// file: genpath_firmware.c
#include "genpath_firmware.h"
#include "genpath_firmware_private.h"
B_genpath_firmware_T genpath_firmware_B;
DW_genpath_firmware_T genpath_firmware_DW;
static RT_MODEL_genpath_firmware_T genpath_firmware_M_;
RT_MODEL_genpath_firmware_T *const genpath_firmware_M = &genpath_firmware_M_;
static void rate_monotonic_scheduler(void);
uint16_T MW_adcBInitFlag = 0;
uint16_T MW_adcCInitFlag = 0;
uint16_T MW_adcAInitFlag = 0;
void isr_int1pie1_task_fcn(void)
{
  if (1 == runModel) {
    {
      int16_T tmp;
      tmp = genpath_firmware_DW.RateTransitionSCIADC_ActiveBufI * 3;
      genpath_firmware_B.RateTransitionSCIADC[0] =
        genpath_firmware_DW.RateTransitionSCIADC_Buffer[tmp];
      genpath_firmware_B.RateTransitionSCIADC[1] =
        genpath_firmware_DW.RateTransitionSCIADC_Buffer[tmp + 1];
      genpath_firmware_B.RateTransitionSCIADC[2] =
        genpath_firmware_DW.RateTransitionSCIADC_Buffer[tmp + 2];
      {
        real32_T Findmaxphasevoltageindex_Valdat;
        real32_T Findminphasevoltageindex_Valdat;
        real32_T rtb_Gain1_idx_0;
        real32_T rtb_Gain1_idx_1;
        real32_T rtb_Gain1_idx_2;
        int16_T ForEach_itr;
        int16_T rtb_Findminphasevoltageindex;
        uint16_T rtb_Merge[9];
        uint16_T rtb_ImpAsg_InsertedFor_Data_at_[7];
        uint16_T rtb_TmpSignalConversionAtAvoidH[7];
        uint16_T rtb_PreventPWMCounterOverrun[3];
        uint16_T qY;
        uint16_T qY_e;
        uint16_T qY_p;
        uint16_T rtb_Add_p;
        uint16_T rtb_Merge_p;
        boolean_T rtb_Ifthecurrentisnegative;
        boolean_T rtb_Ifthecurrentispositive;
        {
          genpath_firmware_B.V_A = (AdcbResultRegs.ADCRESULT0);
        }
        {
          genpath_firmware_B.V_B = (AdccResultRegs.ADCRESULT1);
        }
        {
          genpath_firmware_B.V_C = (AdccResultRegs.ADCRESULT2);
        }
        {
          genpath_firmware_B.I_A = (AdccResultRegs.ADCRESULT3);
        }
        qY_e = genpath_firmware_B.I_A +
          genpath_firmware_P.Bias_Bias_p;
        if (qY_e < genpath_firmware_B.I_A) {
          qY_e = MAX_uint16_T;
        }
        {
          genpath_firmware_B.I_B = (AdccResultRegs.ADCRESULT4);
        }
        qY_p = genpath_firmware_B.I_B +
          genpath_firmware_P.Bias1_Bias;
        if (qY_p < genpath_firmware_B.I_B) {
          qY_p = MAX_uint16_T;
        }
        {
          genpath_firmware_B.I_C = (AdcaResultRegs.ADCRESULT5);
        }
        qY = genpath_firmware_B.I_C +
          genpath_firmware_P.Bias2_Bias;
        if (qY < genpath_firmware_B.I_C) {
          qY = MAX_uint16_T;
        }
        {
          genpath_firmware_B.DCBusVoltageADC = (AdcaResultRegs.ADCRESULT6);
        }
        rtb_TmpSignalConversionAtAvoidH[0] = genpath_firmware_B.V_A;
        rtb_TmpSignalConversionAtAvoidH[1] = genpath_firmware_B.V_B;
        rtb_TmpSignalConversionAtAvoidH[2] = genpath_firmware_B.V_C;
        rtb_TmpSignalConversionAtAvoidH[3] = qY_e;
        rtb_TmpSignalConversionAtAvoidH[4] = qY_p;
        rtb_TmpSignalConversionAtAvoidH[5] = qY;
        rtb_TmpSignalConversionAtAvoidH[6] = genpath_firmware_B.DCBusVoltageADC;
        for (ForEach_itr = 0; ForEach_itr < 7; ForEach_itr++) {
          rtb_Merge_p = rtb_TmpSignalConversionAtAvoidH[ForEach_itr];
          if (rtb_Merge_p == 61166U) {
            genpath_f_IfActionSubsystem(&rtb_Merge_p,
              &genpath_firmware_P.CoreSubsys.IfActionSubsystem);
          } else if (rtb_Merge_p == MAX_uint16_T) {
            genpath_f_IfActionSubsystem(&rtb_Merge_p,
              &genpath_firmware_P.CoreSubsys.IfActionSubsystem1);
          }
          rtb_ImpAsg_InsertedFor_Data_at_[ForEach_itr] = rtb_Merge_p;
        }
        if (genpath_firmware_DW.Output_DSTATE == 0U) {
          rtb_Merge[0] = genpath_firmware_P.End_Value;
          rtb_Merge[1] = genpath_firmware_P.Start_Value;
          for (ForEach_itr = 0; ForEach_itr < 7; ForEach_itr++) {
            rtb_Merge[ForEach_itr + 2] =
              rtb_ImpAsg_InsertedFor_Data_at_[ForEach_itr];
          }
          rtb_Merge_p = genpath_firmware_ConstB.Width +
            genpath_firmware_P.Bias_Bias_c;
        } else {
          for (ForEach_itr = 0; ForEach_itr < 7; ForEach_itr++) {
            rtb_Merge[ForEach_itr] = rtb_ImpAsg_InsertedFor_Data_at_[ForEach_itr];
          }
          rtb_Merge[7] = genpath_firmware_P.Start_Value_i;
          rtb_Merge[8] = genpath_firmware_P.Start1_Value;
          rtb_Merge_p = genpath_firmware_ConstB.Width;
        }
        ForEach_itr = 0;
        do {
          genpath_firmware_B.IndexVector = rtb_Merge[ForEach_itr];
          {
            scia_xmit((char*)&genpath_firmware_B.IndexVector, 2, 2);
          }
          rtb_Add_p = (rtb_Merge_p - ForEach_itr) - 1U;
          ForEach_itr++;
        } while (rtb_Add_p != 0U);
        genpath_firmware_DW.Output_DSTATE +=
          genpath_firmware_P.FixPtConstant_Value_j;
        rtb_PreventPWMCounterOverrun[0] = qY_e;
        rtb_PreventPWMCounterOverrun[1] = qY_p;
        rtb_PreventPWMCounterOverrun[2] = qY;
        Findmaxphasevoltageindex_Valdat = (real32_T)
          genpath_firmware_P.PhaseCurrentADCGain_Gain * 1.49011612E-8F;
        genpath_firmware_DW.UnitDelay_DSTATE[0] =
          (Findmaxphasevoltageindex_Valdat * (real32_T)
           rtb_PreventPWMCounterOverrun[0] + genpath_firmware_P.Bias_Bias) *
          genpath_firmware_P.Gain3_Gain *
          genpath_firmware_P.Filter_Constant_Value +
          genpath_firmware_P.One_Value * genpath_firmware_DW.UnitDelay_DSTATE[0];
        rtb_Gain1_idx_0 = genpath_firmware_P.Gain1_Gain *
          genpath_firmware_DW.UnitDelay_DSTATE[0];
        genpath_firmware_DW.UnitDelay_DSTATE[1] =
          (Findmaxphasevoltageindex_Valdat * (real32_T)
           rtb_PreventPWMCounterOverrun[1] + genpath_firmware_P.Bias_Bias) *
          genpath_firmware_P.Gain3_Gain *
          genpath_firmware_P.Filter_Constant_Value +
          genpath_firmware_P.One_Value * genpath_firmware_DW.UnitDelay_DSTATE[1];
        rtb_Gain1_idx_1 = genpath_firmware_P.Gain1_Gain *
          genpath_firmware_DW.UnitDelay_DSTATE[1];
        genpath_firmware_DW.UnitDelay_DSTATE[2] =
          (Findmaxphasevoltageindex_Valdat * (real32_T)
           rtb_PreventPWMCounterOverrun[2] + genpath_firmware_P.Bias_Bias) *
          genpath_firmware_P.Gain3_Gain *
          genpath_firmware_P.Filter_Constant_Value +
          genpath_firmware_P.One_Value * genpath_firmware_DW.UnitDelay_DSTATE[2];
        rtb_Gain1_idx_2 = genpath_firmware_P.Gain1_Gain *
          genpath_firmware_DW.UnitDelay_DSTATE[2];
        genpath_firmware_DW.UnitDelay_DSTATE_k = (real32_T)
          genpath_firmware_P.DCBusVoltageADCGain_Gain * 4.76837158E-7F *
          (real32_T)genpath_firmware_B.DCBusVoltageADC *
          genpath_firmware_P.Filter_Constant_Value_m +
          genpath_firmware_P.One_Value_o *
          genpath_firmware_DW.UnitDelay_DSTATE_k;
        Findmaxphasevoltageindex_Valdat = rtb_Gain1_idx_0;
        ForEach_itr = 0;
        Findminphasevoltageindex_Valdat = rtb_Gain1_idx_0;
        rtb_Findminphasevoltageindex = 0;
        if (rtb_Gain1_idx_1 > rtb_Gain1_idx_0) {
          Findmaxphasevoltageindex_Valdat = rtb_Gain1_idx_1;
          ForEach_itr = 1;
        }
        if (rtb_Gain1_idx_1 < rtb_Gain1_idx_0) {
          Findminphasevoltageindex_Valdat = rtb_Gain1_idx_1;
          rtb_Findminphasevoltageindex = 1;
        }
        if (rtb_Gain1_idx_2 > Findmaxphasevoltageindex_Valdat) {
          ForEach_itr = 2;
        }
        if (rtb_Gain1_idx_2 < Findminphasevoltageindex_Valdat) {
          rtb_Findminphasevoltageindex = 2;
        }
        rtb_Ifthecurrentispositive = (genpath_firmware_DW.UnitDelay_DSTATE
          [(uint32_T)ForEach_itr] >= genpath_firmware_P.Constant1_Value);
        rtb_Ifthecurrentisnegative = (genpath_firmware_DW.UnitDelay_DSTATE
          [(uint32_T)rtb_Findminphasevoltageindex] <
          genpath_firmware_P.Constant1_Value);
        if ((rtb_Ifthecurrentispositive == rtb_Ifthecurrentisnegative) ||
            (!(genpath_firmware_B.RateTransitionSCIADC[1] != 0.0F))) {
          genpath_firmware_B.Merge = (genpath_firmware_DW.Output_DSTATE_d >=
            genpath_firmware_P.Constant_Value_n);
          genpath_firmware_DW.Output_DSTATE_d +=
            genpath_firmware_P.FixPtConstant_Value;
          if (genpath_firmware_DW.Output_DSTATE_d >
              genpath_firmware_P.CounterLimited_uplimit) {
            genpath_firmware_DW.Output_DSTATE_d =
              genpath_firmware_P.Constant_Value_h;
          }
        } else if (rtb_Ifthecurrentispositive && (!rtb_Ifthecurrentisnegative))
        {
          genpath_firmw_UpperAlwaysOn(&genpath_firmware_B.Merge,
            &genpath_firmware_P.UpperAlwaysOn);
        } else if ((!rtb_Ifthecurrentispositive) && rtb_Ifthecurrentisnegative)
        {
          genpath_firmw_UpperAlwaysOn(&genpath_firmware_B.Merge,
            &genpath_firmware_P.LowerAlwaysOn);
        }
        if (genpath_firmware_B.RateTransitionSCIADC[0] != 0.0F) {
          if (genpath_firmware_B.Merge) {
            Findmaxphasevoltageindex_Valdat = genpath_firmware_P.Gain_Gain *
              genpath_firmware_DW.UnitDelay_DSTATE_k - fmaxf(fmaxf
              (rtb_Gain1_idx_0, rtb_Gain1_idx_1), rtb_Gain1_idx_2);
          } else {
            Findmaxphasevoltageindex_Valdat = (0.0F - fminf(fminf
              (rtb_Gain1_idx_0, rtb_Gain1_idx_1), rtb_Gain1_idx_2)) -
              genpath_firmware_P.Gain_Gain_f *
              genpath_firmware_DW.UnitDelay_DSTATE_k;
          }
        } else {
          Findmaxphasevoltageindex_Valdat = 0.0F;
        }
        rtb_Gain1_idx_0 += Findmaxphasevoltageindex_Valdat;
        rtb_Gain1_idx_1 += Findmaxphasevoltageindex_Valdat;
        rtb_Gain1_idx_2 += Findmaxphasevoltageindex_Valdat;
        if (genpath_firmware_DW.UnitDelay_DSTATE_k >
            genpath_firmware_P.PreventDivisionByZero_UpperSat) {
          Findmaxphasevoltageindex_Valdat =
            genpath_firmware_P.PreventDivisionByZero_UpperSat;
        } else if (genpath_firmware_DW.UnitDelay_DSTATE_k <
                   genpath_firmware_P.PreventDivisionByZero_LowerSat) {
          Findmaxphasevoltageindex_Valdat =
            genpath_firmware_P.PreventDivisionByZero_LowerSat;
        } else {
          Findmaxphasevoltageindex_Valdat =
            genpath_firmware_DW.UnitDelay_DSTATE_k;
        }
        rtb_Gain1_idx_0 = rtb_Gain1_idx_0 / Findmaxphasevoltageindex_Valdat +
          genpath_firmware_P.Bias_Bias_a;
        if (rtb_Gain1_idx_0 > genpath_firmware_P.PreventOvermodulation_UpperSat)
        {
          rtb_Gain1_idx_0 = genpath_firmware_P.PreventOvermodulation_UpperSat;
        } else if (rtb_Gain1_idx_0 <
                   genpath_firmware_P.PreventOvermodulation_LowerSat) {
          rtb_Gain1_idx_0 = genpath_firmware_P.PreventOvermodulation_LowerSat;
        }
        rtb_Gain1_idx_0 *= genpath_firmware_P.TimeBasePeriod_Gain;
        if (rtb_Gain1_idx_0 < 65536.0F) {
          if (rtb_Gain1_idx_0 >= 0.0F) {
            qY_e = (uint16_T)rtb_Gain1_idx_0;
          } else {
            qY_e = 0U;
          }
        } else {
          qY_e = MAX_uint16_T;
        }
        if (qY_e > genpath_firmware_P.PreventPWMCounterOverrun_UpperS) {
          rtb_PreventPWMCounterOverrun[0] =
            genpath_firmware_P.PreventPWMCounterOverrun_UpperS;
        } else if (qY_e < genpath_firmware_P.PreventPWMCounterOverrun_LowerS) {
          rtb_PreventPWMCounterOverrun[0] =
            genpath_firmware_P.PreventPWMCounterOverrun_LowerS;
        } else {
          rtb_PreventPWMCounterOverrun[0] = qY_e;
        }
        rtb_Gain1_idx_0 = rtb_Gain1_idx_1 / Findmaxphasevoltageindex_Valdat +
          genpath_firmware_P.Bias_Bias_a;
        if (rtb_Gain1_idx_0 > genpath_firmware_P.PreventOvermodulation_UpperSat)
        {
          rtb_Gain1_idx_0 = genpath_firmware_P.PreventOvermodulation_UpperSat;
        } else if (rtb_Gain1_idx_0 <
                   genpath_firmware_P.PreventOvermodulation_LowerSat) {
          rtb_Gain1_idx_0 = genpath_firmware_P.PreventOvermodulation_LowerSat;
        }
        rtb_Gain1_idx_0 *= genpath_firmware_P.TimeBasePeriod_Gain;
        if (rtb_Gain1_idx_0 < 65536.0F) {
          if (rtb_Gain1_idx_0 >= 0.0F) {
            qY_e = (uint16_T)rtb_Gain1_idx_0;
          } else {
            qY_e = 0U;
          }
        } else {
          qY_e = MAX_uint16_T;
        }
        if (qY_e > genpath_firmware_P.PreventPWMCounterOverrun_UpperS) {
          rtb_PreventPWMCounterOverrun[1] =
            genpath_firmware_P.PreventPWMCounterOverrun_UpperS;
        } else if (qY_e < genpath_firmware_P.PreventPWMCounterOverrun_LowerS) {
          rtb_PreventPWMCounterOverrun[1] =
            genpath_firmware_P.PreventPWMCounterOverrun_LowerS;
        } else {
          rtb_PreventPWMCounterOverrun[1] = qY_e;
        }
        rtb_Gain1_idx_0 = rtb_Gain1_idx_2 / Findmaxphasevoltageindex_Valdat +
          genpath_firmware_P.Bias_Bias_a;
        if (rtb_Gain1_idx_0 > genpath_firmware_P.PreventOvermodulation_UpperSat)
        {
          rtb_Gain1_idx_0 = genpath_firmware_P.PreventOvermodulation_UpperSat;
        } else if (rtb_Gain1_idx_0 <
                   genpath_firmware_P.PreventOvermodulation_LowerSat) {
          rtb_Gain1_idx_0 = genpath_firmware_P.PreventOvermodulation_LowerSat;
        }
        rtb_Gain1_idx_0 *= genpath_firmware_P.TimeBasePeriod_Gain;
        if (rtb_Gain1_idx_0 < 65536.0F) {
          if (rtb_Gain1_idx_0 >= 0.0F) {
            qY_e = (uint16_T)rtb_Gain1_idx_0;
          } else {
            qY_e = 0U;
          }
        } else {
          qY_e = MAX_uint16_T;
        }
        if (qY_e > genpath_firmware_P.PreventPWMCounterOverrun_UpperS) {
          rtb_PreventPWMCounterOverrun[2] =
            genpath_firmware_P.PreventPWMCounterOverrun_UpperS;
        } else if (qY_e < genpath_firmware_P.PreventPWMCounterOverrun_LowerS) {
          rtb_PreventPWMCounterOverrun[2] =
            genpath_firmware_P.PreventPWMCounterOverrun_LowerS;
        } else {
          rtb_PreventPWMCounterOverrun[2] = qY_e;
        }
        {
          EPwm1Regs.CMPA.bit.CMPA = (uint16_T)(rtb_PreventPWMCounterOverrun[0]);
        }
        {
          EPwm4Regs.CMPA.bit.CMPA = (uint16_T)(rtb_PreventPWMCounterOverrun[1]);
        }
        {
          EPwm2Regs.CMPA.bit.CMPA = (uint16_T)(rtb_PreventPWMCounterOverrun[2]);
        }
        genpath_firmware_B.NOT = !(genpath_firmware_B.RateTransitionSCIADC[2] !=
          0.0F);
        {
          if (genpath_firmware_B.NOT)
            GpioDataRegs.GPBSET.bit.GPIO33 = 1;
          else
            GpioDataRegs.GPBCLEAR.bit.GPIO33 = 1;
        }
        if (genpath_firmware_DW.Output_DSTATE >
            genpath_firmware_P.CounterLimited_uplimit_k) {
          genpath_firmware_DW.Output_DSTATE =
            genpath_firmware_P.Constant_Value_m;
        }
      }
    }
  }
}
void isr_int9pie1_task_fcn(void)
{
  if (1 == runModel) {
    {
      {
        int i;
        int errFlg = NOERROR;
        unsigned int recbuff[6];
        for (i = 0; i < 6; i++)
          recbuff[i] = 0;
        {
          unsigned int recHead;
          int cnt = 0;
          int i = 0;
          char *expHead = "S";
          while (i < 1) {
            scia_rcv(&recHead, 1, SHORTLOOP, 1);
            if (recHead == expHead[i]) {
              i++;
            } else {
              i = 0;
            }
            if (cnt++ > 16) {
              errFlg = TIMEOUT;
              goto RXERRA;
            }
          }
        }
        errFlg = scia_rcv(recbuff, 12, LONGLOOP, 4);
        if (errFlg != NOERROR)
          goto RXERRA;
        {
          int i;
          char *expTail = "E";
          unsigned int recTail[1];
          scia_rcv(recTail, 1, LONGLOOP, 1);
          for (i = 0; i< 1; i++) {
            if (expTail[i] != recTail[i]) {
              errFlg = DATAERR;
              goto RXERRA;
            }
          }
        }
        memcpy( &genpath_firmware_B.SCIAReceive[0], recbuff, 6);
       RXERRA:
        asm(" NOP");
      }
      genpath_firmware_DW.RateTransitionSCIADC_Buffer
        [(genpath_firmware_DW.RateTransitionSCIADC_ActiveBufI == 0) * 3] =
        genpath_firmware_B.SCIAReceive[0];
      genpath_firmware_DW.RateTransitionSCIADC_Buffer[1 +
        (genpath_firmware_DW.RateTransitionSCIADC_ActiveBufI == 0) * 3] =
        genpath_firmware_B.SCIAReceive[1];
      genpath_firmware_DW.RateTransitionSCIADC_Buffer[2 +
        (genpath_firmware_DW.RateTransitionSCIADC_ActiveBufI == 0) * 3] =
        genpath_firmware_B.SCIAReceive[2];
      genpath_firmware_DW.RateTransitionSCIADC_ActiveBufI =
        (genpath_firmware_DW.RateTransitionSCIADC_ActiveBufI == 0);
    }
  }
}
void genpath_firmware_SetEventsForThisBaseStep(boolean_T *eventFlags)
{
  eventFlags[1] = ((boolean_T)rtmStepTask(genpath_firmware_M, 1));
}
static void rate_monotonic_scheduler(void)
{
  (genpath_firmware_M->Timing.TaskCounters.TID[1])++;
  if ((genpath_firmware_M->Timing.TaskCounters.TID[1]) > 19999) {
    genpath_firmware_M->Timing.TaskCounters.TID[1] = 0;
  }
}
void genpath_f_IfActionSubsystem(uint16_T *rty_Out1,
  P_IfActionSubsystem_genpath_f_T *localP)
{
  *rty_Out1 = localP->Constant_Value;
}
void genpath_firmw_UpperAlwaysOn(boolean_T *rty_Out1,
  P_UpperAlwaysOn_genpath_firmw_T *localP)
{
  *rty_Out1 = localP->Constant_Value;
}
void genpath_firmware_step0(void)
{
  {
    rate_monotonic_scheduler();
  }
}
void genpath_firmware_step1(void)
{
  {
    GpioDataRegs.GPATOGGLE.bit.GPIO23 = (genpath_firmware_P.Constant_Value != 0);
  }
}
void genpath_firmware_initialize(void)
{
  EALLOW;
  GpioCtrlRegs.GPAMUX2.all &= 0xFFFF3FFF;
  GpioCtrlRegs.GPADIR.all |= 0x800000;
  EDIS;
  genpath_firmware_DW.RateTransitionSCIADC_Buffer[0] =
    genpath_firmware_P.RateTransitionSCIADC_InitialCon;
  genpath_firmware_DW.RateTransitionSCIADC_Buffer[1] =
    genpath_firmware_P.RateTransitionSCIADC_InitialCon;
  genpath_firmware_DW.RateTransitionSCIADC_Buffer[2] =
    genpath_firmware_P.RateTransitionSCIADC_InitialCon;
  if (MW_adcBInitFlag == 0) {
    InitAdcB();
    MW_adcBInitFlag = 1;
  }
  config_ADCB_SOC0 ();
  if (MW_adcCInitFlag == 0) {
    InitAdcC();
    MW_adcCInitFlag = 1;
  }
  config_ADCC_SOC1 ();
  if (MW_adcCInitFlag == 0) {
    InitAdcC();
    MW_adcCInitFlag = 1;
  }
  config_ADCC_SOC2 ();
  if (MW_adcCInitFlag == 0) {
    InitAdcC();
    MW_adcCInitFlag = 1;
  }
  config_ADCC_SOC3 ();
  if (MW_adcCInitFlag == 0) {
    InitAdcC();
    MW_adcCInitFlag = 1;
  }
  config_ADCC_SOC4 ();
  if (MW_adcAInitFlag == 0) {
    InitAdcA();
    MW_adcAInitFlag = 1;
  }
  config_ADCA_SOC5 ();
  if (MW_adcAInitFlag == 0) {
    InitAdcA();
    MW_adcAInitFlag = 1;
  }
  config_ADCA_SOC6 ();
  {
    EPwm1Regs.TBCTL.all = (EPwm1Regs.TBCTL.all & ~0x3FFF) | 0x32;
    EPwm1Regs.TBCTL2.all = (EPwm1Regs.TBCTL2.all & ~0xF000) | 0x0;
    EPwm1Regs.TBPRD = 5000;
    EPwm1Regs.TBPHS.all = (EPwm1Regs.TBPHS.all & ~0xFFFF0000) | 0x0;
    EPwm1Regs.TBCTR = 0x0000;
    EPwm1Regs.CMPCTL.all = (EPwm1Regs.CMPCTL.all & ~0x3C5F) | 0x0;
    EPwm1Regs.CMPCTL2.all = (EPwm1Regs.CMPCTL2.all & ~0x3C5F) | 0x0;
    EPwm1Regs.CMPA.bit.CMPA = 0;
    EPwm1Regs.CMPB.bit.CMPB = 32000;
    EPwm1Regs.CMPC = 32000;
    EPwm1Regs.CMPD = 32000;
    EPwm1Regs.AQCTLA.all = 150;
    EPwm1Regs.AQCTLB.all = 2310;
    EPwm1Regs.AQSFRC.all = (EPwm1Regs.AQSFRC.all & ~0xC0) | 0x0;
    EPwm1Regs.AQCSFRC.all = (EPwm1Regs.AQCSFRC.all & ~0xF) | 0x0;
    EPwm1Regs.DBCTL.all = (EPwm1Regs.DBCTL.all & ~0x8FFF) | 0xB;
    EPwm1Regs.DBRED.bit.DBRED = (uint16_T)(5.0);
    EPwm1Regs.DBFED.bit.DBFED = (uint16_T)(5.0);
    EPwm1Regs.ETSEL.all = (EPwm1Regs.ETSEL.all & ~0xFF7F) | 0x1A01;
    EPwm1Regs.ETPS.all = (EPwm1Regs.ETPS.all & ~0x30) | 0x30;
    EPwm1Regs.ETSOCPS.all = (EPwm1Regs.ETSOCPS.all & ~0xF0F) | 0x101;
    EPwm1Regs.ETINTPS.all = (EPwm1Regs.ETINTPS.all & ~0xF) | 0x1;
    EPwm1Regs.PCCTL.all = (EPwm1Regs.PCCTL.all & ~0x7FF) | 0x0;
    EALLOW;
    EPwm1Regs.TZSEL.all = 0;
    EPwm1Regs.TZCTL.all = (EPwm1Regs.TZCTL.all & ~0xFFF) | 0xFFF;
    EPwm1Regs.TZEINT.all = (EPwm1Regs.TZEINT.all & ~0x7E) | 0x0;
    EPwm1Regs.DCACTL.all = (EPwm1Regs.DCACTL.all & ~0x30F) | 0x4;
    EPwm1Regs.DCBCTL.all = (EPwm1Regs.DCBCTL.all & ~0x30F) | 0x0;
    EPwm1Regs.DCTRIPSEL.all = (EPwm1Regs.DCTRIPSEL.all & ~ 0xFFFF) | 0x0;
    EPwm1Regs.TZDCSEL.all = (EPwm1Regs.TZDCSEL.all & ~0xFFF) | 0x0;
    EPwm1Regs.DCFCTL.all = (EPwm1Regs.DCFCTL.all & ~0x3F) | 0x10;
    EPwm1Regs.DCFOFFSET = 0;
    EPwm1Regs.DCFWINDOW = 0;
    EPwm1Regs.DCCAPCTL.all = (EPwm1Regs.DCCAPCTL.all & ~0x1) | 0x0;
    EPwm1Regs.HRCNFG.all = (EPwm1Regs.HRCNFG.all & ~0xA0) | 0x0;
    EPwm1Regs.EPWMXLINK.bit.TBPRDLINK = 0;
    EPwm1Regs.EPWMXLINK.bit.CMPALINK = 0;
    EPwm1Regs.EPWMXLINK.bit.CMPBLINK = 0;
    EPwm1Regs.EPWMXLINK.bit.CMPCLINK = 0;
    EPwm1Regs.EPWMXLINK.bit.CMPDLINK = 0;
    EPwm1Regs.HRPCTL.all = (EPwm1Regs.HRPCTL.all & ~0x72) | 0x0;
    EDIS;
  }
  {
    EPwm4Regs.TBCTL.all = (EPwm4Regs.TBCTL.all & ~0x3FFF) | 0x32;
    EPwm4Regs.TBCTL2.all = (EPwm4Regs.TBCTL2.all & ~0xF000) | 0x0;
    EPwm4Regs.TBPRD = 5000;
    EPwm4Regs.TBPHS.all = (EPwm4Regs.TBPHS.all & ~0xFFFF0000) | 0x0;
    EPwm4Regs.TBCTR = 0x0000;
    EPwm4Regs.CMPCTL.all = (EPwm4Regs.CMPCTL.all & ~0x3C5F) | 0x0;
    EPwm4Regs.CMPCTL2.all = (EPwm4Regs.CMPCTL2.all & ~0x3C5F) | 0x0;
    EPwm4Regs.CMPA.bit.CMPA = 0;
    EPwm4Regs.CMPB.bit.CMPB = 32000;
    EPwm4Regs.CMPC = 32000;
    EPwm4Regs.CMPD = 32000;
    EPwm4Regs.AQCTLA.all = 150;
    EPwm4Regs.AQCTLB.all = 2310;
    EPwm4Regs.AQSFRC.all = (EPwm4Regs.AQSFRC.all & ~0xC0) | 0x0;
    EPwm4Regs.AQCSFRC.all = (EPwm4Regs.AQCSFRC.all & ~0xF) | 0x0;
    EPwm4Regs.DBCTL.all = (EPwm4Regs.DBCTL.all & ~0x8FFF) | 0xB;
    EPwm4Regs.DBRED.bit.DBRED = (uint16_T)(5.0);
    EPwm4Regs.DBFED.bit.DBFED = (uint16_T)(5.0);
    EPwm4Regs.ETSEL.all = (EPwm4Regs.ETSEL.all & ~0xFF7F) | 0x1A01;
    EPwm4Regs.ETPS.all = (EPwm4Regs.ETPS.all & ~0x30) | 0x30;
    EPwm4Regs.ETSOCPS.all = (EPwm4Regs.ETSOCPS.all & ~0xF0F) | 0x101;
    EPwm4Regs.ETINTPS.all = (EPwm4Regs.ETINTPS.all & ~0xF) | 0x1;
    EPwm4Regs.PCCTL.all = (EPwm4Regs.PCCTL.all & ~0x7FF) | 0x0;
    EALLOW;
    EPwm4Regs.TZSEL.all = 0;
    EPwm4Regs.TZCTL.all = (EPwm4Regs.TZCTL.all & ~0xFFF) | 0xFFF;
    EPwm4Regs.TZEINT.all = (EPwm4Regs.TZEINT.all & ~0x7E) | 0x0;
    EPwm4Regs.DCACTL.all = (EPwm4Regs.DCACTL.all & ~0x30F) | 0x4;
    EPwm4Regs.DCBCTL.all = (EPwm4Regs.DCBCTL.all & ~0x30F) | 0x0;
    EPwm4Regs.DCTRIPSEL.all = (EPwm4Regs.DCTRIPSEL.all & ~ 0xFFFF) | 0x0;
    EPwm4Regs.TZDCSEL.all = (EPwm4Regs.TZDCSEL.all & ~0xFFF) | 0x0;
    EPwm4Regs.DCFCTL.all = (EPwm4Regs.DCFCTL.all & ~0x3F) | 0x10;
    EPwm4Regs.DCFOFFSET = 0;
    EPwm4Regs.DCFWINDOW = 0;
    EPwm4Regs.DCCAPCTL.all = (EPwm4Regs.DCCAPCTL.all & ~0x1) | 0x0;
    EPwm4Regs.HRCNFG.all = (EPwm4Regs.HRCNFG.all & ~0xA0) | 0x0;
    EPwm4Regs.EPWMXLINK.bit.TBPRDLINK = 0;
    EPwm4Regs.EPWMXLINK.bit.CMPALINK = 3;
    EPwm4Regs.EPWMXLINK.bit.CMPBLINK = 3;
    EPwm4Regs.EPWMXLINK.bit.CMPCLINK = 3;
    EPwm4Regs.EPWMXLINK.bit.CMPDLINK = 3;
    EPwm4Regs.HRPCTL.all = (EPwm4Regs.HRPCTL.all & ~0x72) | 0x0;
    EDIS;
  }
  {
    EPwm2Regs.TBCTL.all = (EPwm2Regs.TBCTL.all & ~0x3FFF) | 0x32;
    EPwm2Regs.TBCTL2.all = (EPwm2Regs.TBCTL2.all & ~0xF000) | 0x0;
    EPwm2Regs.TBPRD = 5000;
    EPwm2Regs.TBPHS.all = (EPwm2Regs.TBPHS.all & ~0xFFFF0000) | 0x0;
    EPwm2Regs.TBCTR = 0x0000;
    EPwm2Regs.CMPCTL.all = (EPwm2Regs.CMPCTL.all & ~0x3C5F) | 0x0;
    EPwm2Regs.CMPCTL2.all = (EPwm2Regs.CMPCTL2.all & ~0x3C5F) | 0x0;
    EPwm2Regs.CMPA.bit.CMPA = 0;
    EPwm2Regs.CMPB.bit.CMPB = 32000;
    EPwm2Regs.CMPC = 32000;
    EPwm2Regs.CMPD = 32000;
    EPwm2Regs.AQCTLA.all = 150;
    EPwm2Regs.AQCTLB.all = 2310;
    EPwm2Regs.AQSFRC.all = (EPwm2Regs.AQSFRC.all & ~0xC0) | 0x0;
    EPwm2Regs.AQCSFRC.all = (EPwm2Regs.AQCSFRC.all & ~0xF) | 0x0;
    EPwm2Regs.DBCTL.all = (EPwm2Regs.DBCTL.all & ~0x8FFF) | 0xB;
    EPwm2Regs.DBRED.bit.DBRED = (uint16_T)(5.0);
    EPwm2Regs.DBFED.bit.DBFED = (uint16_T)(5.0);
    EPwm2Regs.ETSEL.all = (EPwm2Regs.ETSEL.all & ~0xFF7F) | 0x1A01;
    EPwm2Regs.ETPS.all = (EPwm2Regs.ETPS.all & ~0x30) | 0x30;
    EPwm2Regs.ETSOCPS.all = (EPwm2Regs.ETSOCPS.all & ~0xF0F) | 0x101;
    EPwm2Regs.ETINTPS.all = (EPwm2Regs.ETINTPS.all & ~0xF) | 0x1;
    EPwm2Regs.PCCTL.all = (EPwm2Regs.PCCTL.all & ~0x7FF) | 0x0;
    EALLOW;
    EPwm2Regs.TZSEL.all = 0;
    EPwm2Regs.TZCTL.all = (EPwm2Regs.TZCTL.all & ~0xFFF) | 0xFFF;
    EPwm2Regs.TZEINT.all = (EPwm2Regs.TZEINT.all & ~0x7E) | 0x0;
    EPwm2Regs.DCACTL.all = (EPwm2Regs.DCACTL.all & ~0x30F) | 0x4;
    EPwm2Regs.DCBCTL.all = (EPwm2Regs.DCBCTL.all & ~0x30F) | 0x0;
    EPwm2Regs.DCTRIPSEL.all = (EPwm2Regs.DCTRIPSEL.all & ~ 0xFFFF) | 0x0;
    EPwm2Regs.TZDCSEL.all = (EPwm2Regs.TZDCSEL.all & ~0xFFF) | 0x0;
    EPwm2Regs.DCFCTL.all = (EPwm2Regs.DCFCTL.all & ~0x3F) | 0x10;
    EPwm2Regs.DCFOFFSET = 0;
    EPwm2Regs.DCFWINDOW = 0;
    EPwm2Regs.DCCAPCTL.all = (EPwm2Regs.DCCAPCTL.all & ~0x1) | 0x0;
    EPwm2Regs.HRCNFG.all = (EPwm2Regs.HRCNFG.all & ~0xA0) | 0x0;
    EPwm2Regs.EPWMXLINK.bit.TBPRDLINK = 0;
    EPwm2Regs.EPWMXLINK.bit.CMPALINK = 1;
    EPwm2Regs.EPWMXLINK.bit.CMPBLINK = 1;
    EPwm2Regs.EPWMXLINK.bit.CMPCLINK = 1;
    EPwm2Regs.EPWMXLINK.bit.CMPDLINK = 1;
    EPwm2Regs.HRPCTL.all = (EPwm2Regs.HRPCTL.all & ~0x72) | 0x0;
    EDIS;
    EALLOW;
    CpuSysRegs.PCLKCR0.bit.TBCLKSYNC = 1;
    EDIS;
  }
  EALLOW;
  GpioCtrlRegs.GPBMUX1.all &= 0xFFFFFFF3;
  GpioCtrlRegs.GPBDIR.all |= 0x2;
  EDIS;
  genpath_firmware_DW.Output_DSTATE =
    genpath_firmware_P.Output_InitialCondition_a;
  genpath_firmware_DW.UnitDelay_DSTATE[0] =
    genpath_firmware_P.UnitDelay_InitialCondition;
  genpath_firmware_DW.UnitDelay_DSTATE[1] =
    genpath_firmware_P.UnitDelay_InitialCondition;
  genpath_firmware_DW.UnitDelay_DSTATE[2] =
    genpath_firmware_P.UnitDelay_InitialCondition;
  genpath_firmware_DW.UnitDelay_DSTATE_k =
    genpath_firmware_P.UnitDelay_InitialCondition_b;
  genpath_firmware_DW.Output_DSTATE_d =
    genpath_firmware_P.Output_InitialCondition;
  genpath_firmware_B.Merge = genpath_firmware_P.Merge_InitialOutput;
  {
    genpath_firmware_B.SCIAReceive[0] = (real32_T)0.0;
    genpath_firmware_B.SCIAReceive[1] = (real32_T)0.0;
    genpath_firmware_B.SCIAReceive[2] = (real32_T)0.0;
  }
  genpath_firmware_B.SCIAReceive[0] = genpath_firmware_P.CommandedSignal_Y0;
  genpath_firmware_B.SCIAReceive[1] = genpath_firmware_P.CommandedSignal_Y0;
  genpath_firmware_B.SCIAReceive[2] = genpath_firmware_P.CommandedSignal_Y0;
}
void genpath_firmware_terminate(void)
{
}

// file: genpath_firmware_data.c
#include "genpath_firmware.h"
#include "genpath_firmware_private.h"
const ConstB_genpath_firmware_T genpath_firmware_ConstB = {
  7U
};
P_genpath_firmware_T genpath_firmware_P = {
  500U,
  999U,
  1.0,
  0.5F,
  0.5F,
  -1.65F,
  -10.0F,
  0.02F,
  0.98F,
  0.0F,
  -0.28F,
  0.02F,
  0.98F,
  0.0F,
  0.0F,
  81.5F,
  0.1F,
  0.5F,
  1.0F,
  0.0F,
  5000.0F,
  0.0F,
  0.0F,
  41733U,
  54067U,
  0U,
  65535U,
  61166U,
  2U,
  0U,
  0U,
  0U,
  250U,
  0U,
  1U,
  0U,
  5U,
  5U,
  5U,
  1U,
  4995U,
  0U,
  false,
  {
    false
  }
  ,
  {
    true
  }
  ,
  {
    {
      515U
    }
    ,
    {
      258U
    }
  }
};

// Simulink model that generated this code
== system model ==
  Subsystem#1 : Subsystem  <- 1: RateTransitionSCIADC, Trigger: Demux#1
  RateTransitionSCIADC : RateTransition  <- 1: Subsystem#2
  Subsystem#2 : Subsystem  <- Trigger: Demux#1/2
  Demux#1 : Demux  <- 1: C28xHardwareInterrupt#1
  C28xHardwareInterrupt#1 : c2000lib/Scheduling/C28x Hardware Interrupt
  DigitalOutput#1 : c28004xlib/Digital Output  <- 1: Constant
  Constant : Constant
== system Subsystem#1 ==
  CommandedSignal : Inport
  TriggerPort#1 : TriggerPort  TriggerType=function-call
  IIRFilter#1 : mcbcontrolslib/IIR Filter  <- 1: Gain#1
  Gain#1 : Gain  Gain=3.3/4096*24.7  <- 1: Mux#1
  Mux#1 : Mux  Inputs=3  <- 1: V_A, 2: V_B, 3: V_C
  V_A : c2802xlib/ADC
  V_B : c2802xlib/ADC
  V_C : c2802xlib/ADC
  Subsystem#3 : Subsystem  <- 1: Merge, 2: Merge#1
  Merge : Merge  <- 1: Start, 2: Data
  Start : Subsystem  <- 1: Subsystem#4, 2: Width, Action: If#1
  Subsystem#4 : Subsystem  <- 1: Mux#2
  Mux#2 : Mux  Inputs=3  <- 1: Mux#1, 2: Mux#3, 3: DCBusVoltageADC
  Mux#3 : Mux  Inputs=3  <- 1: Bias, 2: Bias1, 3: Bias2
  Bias : Bias  Bias=+5  <- 1: I_A
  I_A : c2802xlib/ADC
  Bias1 : Bias  Bias=+5  <- 1: I_B
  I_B : c2802xlib/ADC
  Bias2 : Bias  Bias=+5  <- 1: I_C
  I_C : c2802xlib/ADC
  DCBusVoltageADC : c2802xlib/ADC
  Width : Width  <- 1: Subsystem#4
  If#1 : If  IfExpression=u1 == 0  <- 1: CounterLimited
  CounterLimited : simulink/Sources/Counter Limited  uplimit=999
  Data : Subsystem  <- 1: Subsystem#4, 2: Width, Action: If#1/2
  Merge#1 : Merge  <- 1: Start/2, 2: Data/2
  ePWM#1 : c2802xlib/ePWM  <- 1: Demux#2
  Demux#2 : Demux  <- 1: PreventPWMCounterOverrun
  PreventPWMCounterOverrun : Saturate  UpperLimit=4995  LowerLimit=0  <- 1: DataTypeConversion#1
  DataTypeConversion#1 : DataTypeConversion  <- 1: TimeBasePeriod
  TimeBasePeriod : Gain  Gain=5000  <- 1: PreventOvermodulation
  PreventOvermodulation : Saturate  UpperLimit=1  LowerLimit=0  <- 1: Bias#1
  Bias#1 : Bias  Bias=0.5  <- 1: Product#1
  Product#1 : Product  Inputs=*/  <- 1: Add, 2: PreventDivisionByZero
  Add : Sum  <- 1: Gain1, 2: Merge#2
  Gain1 : Gain  Gain=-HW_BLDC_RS  <- 1: IIRFilter#2
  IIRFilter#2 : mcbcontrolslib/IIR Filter  <- 1: Gain3
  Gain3 : Gain  Gain=-10  <- 1: Bias#2
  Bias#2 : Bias  Bias=-1.65  <- 1: PhaseCurrentADCGain
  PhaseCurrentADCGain : Gain  Gain=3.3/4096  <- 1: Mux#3
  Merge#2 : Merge  <- 1: Subsystem#5, 2: Subsystem#6
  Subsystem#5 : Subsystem  <- 1: Gain1, 2: IIRFilter#3, 3: Merge#3, Action: If#2
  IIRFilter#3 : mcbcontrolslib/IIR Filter  <- 1: DCBusVoltageADCGain
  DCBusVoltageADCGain : Gain  Gain=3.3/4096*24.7  <- 1: DCBusVoltageADC
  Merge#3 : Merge  Inputs=3  <- 1: Subsystem#7, 2: UpperAlwaysOn, 3: LowerAlwaysOn
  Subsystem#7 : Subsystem  <- Action: If#3
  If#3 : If  IfExpression=(u1 == u2) | ~u3  ElseIfExpressions=u1 & ~u2,~u1 & u2  <- 1: Ifthecurrentispositive, 2: Ifthecurrentisnegative, 3: DataTypeConversion#2
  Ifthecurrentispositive : RelationalOperator  <- 1: MultiPortSwitch#1, 2: Constant1
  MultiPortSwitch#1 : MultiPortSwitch  DataPortOrder=Zero-based contiguous  Inputs=1  <- 1: Findmaxphasevoltageindex, 2: IIRFilter#2
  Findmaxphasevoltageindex : dspstat3/Maximum  <- 1: Gain1
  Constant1 : Constant  Value=0
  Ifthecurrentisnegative : RelationalOperator  Operator=<  <- 1: MultiPortSwitch#2, 2: Constant1
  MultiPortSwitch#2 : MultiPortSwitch  DataPortOrder=Zero-based contiguous  Inputs=1  <- 1: Findminphasevoltageindex, 2: IIRFilter#2
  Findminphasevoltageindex : dspstat3/Minimum  <- 1: Gain1
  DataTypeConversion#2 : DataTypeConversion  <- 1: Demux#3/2
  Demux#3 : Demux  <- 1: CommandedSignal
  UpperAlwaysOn : Subsystem  <- Action: If#3/2
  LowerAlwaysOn : Subsystem  <- Action: If#3/3
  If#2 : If  IfExpression=u1  <- 1: DataTypeConversion#3
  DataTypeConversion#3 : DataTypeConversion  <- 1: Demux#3
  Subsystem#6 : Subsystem  <- Action: If#2/2
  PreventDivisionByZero : Saturate  UpperLimit=81.5  LowerLimit=0.1  <- 1: IIRFilter#3
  ePWM#2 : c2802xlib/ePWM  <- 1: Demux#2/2
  ePWM#3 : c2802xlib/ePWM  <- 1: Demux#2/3
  DigitalOutput#2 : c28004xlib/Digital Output  <- 1: NOT
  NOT : Logic  Operator=NOT  <- 1: DataTypeConversion#4
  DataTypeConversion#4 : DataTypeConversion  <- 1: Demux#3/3
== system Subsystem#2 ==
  TriggerPort#2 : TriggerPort  TriggerType=function-call
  Outport#1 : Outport  <- 1: SCIAReceive
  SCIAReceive : c280xlib/SCI Receive
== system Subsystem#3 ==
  Inport#1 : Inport
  Inport#2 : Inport
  WhileIterator#1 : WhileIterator  MaxIters=-1  WhileBlockType=do-while  <- 1: Sum#1
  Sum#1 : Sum  Inputs=+-  <- 1: Inport#2, 2: WhileIterator#1
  SCITransmit#1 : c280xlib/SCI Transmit  <- 1: IndexVector
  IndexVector : MultiPortSwitch  Inputs=1  <- 1: WhileIterator#1, 2: Inport#1
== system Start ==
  Inport#3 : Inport
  Inport#4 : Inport
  ActionPort#1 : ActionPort
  Outport#2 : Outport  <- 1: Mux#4
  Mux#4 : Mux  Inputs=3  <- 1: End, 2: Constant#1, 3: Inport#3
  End : Constant  Value=65535
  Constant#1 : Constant  Value=61166
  Outport#3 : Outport  <- 1: Bias#3
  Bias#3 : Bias  Bias=2  <- 1: Inport#4
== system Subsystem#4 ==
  Inport#5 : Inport
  ForEach : ForEach
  Outport#4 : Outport  <- 1: Merge#4
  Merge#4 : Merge  Inputs=3  <- 1: IfActionSubsystem, 2: IfActionSubsystem1, 3: Subsystem#8
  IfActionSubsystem : Subsystem  <- Action: If#4
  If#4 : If  IfExpression=u1 == 61166  ElseIfExpressions=u1 == 65535  <- 1: Inport#5
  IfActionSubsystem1 : Subsystem  <- Action: If#4/2
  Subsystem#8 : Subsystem  <- 1: Inport#5, Action: If#4/3
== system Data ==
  Inport#6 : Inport
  Inport#7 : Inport
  ActionPort#2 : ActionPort
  Outport#5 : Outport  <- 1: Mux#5
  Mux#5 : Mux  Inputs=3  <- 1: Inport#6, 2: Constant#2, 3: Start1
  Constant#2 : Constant  Value=0
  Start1 : Constant  Value=0
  Outport#6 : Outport  <- 1: Inport#7
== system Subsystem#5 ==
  Inport#8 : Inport
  Inport#9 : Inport
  Inport#10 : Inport
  ActionPort#3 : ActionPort
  Outport#7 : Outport  <- 1: Merge#5
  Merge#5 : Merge  <- 1: Subsystem#9, 2: Subsystem#10
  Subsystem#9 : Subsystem  <- 1: Inport#8, 2: Inport#9, Action: If#5
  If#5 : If  IfExpression=u1  <- 1: Inport#10
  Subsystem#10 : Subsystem  <- 1: Inport#8, 2: Inport#9, Action: If#5/2
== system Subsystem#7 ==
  ActionPort#4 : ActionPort
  Out1 : Outport  <- 1: RelationalOperator#1
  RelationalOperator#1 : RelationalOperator  <- 1: CounterLimited#1, 2: Constant#3
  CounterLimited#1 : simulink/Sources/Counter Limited  uplimit=500
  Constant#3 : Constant  Value=250
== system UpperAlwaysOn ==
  ActionPort#5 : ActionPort
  Outport#8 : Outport  <- 1: Constant#4
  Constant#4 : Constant  Value=true
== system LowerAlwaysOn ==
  ActionPort#6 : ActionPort
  Outport#9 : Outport  <- 1: Constant#5
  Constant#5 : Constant  Value=false
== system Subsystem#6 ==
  ActionPort#7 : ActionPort
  Outport#10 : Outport
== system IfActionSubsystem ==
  ActionPort#8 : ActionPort
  Outport#11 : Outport  <- 1: Constant#6
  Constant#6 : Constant  Value=258
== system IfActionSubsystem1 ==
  ActionPort#9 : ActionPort
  Outport#12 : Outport  <- 1: Constant#7
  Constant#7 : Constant  Value=515
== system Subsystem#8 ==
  Inport#11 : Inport
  ActionPort#10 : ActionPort
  Outport#13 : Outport  <- 1: Inport#11
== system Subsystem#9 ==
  Inport#12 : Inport
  Inport#13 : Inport
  ActionPort#11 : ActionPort
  Outport#14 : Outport  <- 1: Sum#2
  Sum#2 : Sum  Inputs=-+  <- 1: MinMax#1, 2: Gain
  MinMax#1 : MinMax  Function=max  <- 1: Inport#12
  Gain : Gain  Gain=1/2  <- 1: Inport#13
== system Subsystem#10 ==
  Inport#14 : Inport
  Inport#15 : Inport
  ActionPort#12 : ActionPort
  Outport#15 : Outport  <- 1: Sum#3
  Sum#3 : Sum  Inputs=--  <- 1: MinMax#2, 2: Gain#2
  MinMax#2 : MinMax  <- 1: Inport#14
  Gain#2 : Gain  Gain=1/2  <- 1: Inport#15
